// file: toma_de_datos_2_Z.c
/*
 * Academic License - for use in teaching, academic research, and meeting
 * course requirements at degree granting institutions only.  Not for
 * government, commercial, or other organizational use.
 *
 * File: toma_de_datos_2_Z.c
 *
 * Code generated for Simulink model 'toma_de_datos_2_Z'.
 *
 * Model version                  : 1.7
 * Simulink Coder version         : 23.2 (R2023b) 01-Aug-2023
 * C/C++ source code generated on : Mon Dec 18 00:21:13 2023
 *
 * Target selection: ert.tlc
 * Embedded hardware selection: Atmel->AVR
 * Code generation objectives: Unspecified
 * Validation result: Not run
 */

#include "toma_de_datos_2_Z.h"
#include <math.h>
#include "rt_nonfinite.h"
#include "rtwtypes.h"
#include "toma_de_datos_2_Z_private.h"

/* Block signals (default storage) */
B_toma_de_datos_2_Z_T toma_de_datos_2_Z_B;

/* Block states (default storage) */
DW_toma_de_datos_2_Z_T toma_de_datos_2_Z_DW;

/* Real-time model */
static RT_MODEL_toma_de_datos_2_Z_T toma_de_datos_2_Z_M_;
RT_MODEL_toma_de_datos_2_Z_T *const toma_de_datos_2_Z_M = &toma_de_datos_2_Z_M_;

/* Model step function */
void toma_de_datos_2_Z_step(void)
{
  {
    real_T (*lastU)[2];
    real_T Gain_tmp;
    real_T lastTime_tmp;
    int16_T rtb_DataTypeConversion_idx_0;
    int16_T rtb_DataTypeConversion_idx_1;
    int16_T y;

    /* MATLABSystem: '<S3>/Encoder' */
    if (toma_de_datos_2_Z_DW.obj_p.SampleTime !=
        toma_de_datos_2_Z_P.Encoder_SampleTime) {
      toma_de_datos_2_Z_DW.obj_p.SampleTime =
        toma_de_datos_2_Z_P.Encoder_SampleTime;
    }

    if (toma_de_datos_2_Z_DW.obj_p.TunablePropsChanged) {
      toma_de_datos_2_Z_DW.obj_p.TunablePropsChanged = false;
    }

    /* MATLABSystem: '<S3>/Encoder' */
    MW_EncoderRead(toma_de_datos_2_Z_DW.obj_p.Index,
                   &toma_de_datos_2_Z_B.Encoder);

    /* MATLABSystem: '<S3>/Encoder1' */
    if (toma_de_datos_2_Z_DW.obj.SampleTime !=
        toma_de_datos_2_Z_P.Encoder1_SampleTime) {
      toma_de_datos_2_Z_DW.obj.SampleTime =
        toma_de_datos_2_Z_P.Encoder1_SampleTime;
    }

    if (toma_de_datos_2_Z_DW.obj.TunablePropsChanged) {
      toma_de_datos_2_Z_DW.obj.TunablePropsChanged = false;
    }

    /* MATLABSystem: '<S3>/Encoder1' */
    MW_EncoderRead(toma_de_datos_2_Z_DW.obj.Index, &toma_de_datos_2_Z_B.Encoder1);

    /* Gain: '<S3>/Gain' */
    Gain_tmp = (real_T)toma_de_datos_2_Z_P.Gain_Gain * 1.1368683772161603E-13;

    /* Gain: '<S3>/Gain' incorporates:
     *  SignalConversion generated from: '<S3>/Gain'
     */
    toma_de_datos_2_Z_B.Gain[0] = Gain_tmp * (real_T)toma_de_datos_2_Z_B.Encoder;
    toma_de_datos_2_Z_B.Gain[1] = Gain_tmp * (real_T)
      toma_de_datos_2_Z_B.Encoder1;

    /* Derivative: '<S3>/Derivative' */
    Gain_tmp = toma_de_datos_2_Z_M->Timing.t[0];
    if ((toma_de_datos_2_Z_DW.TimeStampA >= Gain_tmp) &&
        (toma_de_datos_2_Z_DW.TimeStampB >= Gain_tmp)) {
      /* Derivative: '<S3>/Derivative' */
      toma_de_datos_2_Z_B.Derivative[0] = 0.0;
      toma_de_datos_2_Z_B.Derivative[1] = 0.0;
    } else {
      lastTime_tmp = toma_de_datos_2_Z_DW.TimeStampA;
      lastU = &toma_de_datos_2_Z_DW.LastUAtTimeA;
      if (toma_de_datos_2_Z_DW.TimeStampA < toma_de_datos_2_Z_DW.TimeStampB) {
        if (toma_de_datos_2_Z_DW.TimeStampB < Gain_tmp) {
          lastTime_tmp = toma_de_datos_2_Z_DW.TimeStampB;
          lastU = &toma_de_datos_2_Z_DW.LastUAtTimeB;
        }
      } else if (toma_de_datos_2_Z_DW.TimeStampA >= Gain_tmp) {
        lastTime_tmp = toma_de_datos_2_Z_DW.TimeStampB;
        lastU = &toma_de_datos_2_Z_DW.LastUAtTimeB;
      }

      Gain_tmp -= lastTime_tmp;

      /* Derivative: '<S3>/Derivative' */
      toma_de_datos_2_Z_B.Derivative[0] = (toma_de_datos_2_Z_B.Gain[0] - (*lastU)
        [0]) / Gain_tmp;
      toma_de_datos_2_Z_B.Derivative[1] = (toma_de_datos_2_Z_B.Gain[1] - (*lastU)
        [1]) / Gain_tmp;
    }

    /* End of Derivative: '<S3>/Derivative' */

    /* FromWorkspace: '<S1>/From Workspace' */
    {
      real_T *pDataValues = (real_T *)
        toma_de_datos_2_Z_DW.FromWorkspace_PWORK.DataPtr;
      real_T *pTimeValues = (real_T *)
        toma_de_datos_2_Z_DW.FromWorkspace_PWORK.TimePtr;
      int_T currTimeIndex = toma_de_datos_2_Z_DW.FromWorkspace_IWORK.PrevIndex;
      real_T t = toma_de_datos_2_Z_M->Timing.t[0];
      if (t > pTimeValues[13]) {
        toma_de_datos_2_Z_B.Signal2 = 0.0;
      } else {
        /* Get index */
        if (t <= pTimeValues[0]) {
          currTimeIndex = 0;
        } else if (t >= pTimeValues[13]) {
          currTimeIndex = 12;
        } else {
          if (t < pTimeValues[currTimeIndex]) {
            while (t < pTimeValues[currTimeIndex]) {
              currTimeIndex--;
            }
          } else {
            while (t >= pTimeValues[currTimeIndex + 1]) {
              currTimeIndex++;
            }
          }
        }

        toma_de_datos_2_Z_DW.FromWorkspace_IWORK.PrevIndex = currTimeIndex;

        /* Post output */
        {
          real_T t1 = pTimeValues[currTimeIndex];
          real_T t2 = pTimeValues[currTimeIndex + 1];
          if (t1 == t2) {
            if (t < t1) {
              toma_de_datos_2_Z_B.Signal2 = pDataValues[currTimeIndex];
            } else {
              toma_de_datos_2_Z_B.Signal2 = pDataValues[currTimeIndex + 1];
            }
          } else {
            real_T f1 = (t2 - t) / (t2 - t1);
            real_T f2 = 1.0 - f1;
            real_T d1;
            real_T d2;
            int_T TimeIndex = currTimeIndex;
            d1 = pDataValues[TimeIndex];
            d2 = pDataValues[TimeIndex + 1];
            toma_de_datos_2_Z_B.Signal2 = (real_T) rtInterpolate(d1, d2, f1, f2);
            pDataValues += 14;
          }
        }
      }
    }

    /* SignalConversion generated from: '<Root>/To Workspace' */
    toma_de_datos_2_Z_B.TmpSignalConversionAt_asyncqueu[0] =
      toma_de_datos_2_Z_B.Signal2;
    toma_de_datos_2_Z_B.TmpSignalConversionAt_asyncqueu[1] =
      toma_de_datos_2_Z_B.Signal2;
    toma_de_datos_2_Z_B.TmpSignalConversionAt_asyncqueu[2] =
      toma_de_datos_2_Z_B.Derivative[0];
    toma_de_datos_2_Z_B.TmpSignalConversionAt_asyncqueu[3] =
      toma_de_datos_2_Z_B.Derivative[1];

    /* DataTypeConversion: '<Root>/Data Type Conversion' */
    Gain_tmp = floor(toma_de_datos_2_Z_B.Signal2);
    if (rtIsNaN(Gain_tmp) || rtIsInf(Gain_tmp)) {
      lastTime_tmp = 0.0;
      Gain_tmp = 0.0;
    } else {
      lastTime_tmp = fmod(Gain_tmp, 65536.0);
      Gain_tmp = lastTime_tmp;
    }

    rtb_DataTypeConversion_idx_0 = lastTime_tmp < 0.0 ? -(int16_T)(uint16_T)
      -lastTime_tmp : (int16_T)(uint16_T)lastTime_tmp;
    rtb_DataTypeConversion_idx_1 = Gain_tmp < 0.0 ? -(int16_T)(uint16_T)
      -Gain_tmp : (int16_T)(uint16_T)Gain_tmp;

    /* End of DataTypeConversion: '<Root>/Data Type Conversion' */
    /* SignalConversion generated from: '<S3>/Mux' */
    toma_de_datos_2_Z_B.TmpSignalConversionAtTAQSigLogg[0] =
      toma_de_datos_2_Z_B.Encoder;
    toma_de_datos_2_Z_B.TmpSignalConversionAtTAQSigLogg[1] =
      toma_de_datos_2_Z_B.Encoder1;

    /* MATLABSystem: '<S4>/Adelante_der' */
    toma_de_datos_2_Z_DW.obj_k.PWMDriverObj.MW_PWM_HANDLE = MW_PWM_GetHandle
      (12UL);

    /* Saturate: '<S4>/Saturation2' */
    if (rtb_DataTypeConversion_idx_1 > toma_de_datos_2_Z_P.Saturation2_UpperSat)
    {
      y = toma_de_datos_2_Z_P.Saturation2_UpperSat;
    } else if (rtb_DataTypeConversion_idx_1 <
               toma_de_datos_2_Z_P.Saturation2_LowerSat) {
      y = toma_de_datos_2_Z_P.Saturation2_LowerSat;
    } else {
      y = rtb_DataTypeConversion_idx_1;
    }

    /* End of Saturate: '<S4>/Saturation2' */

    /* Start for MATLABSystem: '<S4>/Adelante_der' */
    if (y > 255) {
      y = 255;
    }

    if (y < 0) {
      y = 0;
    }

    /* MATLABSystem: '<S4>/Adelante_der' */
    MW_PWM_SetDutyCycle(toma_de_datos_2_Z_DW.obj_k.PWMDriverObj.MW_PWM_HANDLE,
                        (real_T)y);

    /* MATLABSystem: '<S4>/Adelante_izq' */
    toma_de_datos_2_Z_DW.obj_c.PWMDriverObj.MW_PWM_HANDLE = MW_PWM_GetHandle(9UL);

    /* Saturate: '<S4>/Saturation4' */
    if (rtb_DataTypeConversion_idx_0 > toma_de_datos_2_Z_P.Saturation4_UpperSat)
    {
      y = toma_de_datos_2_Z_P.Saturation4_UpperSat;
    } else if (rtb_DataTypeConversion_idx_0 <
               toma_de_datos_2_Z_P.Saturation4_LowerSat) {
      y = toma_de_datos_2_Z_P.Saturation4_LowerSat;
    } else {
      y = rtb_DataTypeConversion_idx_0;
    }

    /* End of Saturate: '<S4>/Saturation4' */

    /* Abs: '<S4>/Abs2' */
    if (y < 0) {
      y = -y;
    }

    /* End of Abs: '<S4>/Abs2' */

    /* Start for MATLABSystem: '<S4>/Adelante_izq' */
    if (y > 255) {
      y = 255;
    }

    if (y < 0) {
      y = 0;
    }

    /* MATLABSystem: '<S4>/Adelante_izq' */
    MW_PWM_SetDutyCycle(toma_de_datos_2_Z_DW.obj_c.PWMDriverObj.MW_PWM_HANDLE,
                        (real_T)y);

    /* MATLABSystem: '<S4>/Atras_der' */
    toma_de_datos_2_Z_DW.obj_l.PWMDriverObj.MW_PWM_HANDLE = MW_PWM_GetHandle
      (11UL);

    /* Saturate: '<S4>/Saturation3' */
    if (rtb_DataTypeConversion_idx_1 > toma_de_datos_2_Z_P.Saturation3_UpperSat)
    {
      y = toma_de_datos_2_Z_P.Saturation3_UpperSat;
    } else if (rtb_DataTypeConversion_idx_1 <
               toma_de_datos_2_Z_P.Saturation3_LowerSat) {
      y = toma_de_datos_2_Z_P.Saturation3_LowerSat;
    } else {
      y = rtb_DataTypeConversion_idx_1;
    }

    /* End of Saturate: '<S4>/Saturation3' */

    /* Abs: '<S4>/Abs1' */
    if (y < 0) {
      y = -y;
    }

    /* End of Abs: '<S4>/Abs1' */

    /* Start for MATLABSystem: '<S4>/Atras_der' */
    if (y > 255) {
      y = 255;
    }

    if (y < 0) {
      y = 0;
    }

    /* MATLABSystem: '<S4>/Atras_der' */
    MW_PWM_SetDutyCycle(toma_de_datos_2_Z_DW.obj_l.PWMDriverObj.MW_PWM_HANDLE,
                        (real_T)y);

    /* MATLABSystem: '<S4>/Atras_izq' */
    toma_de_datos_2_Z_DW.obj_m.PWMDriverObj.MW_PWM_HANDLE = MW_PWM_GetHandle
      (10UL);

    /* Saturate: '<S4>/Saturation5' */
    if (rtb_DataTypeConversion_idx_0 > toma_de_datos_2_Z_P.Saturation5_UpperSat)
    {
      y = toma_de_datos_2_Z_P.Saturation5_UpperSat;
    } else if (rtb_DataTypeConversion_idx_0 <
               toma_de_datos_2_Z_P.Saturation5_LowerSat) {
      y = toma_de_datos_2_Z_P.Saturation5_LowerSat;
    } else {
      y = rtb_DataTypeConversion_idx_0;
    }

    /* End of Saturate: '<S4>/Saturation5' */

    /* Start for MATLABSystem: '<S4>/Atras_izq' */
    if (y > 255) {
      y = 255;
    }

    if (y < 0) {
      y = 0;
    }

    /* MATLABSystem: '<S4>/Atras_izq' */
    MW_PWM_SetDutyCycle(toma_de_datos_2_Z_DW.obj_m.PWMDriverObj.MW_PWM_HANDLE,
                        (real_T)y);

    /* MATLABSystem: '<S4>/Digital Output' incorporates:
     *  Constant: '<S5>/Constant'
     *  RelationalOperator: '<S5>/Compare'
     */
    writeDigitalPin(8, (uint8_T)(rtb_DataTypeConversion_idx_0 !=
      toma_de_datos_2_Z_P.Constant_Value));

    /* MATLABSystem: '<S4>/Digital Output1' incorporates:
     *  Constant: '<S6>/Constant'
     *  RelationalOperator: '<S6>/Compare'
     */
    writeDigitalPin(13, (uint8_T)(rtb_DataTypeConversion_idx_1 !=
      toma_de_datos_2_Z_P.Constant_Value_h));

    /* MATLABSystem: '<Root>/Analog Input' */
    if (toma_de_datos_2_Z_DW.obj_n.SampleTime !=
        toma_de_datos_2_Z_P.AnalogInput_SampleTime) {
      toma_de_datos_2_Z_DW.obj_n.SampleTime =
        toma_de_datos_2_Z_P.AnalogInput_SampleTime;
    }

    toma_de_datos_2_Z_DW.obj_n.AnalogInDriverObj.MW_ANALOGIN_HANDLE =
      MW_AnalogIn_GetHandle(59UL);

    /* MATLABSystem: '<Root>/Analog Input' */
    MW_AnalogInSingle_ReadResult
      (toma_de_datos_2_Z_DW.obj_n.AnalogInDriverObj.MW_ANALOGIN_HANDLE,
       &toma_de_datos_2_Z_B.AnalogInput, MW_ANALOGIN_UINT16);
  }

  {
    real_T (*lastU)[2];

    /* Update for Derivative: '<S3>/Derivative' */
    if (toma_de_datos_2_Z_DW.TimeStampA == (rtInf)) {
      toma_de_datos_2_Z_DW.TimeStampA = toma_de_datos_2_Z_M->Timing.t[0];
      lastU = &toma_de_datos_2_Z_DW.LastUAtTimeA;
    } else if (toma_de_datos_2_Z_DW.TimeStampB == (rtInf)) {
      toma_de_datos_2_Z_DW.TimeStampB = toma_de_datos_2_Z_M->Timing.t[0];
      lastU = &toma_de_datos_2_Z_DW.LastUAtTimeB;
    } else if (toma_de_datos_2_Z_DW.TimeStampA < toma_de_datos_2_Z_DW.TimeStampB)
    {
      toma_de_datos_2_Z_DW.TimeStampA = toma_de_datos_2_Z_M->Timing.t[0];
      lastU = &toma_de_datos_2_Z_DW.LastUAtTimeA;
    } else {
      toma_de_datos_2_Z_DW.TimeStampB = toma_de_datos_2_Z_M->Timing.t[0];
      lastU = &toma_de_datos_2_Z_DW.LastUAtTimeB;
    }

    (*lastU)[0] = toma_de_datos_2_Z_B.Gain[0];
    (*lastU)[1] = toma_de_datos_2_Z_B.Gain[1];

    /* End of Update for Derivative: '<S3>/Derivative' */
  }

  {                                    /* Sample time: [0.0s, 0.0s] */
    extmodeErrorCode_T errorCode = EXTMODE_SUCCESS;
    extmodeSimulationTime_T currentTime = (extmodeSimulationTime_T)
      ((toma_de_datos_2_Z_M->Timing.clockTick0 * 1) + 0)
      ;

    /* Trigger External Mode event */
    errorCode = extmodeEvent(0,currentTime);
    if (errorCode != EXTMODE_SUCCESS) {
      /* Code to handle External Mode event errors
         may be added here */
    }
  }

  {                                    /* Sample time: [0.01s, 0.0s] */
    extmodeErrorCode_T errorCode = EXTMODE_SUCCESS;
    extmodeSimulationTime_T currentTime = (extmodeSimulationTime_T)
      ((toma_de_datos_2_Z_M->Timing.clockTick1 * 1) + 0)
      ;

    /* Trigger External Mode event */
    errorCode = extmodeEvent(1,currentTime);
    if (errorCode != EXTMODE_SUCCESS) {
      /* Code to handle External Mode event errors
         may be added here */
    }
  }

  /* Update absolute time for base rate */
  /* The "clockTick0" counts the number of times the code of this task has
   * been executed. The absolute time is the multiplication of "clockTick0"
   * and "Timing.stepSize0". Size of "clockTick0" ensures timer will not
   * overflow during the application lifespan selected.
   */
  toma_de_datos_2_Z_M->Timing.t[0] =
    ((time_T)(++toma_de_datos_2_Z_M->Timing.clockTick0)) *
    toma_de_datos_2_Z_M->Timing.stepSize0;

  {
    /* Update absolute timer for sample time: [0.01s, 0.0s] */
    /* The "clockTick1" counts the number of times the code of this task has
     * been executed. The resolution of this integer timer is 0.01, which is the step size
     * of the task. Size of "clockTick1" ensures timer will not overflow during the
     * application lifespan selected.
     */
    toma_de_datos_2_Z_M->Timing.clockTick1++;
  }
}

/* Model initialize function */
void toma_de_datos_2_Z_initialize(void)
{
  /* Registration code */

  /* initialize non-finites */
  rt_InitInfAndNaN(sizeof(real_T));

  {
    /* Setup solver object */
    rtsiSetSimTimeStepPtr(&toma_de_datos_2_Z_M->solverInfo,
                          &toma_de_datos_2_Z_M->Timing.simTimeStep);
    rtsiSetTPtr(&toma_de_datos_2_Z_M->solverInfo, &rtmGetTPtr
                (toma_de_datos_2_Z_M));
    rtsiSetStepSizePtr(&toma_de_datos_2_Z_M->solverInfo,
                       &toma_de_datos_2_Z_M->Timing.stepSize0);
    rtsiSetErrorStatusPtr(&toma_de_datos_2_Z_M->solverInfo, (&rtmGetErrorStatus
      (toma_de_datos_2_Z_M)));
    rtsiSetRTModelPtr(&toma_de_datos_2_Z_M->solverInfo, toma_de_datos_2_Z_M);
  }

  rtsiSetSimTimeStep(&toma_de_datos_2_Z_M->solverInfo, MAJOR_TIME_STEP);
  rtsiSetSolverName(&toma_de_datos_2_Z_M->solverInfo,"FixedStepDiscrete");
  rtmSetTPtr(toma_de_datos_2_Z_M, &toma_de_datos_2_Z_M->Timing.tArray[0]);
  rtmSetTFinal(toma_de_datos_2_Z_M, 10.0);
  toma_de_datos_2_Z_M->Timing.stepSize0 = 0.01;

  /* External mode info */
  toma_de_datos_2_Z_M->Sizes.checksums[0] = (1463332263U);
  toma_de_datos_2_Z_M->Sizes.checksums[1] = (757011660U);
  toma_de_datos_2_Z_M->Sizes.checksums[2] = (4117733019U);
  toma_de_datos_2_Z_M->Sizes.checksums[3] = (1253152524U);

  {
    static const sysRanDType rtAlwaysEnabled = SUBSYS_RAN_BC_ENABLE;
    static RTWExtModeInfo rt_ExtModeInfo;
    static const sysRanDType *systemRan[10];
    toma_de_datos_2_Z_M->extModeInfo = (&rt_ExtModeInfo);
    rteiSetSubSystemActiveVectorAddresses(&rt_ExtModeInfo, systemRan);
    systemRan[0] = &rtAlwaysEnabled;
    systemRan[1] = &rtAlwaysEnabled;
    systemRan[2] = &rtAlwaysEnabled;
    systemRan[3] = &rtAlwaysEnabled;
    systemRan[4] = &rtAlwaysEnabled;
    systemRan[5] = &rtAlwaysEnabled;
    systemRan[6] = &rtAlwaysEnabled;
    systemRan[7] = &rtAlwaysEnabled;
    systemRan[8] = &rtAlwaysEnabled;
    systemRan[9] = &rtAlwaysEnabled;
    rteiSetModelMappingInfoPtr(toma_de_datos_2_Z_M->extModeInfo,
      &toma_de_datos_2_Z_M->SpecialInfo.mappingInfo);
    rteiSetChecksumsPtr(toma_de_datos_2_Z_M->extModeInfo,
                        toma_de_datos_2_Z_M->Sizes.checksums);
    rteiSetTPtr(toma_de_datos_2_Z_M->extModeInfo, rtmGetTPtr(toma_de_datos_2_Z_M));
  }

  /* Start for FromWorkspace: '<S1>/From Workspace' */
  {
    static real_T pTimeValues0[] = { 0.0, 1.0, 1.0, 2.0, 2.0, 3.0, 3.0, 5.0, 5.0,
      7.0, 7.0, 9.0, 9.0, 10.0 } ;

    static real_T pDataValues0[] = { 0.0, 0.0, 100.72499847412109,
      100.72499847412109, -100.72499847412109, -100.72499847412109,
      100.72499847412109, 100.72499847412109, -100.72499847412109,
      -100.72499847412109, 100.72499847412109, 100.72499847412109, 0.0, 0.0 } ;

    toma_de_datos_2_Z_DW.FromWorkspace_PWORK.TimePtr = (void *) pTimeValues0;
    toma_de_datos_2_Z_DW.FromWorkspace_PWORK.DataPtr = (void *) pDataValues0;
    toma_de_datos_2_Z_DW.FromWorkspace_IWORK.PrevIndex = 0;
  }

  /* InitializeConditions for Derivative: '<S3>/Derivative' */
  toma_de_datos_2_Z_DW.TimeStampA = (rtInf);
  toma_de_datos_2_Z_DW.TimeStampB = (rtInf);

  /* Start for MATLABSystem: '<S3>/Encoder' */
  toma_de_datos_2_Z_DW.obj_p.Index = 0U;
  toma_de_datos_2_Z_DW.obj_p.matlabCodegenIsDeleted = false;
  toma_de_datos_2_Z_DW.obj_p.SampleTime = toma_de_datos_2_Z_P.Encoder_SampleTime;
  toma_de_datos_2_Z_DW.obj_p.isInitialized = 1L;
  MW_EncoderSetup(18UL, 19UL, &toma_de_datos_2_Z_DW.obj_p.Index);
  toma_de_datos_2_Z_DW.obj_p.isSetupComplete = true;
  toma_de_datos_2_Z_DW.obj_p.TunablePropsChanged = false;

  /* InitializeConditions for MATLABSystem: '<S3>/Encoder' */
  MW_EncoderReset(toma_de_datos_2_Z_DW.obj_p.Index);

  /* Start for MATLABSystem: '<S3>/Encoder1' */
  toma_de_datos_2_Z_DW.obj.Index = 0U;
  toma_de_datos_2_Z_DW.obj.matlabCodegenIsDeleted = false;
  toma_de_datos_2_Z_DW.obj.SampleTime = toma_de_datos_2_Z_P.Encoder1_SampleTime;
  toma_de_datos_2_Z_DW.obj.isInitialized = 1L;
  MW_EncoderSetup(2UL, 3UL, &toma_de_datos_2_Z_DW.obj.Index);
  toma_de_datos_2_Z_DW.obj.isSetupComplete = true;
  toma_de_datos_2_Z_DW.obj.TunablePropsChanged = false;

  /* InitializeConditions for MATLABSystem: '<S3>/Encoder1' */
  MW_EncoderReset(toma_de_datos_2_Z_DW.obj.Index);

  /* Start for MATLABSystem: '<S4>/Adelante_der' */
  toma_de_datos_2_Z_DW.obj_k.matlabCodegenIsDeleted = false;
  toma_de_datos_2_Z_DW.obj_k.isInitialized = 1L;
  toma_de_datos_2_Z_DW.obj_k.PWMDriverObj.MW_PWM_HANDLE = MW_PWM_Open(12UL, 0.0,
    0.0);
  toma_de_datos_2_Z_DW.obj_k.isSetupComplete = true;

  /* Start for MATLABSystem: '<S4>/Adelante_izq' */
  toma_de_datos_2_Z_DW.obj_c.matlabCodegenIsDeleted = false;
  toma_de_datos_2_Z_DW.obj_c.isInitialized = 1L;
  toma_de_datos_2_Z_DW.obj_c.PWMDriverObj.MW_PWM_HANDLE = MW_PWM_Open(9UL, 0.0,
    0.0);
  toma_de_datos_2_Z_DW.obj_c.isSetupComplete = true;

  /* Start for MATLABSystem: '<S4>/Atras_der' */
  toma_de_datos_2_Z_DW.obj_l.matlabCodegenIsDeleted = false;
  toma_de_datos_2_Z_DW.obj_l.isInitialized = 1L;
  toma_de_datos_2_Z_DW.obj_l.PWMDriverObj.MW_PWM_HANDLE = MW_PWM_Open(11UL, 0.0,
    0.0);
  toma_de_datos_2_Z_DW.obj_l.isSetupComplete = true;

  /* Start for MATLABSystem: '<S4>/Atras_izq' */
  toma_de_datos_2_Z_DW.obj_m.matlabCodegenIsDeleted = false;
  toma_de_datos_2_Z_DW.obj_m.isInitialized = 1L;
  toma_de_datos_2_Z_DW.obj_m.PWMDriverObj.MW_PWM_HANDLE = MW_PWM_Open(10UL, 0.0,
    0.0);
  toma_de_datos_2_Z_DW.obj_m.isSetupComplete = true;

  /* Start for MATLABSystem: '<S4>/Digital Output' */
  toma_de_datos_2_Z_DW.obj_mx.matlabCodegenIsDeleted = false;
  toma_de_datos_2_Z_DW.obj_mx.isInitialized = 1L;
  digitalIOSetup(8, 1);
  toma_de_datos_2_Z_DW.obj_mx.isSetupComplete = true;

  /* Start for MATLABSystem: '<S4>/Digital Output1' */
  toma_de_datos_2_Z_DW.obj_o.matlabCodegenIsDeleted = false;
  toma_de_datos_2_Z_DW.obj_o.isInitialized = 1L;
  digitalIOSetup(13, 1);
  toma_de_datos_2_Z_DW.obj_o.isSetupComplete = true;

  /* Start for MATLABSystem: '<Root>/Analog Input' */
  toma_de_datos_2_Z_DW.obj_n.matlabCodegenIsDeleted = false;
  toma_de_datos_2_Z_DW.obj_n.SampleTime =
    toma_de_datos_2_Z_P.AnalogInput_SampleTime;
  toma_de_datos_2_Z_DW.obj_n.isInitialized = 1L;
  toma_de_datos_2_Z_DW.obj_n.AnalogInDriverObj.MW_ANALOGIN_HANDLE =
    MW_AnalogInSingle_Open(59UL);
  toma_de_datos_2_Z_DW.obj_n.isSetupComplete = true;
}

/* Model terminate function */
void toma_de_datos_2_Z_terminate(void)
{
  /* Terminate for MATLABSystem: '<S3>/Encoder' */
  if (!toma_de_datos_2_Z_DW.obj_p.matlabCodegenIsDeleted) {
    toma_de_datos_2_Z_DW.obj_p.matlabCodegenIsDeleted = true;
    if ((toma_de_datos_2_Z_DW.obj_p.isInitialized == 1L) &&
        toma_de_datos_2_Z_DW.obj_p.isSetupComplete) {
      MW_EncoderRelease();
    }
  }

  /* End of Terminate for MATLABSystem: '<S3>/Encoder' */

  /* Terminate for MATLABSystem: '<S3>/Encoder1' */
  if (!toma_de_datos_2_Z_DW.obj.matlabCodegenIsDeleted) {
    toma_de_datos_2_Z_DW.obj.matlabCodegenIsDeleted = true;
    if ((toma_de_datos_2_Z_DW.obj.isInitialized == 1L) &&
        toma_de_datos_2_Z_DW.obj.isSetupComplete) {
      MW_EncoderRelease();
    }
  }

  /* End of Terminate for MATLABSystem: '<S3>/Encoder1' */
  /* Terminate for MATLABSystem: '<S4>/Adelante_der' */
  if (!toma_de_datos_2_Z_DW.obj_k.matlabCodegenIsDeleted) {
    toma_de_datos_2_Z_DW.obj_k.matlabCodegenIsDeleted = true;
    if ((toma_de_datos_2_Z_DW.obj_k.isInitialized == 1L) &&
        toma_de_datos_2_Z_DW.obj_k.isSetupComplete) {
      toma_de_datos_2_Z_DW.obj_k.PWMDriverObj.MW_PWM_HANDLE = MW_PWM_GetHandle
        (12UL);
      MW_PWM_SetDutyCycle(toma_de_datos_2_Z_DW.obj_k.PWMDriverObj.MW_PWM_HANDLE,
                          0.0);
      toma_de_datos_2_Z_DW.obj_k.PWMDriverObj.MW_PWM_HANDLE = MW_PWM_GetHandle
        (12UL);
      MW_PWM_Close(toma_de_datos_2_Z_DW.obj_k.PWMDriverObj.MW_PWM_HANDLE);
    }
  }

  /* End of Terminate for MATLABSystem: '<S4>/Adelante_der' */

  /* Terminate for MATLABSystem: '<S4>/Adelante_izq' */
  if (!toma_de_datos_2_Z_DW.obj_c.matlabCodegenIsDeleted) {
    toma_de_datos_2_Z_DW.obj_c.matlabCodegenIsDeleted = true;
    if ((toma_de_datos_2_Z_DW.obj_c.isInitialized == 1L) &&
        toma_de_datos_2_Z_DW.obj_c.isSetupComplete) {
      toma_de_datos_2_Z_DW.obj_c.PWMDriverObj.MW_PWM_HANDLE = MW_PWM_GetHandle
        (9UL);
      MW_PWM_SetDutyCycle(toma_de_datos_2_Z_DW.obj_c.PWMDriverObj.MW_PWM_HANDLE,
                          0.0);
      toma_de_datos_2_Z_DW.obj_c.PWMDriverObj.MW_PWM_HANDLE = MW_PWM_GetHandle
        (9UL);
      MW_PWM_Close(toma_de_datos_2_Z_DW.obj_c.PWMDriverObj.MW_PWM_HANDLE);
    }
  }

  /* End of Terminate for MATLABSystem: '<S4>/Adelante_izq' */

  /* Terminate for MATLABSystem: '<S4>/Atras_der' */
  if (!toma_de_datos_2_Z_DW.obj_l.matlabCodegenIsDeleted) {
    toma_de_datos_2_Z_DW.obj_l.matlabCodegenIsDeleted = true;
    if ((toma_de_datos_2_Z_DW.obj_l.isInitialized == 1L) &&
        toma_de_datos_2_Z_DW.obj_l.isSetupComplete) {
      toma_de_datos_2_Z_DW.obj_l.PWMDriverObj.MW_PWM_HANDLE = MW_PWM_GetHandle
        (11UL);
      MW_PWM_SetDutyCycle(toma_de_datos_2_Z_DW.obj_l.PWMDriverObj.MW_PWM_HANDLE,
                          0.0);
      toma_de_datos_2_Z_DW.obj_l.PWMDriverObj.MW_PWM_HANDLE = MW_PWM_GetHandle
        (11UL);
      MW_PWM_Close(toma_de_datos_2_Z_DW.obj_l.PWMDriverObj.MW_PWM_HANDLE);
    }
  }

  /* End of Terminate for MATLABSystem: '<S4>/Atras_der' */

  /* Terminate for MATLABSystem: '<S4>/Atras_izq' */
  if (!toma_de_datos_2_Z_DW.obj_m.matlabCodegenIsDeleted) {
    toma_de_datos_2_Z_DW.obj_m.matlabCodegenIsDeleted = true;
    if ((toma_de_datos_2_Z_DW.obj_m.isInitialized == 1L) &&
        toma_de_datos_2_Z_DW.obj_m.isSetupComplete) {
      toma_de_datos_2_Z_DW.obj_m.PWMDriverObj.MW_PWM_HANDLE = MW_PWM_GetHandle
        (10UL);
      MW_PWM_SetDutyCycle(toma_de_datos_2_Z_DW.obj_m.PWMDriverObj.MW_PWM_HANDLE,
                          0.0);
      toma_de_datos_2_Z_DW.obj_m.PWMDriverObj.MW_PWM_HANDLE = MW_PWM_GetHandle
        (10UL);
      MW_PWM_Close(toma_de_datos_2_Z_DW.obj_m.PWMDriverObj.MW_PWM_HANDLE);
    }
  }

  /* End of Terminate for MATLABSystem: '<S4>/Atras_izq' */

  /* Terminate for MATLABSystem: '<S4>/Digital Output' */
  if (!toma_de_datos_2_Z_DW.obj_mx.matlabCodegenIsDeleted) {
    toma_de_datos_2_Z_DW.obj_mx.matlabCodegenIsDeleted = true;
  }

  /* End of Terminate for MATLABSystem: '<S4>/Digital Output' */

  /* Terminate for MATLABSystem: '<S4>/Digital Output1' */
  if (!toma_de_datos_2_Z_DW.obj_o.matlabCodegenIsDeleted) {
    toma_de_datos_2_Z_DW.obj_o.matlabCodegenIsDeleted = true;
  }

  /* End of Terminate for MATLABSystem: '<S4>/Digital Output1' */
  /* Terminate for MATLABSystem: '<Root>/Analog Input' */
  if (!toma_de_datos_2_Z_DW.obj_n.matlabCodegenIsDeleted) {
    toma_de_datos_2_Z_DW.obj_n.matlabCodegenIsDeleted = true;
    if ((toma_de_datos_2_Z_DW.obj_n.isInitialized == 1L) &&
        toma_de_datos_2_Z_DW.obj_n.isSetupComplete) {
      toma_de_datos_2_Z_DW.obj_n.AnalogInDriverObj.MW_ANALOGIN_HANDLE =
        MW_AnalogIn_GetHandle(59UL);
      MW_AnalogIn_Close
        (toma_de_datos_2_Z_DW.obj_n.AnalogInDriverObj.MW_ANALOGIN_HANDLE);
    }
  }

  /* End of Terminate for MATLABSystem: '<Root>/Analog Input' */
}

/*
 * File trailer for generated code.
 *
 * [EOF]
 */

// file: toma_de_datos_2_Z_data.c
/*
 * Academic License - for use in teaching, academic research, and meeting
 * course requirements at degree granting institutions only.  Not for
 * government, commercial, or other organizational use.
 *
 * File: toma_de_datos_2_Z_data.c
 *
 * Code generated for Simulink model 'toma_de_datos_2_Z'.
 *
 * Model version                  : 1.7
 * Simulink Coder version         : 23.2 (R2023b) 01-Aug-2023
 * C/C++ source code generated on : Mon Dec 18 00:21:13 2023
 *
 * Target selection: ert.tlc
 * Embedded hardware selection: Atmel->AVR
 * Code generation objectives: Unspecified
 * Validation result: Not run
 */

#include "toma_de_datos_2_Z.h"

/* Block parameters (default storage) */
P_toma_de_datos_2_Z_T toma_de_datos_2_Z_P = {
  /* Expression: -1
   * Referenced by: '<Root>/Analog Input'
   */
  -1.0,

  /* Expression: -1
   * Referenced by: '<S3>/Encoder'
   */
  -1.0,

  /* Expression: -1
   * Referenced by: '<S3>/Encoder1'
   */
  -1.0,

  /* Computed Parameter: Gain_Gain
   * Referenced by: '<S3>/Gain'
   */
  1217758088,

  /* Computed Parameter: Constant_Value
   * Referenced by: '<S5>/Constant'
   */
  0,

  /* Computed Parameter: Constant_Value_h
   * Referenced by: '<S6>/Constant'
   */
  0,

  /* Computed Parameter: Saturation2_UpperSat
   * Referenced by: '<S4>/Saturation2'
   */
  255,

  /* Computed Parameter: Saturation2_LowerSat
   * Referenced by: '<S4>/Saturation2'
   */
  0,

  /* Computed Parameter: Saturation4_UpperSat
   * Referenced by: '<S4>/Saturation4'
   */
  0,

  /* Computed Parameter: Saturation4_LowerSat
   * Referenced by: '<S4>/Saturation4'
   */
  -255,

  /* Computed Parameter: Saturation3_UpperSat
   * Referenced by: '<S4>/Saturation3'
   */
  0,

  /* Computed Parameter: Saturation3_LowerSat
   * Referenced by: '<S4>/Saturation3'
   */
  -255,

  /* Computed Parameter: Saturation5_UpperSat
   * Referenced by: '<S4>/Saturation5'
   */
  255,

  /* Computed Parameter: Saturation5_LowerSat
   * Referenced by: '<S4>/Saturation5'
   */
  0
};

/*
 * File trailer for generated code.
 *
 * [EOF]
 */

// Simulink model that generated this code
simulink model "toma_de_datos_2_Z"  (R2023b)
settings: Solver=FixedStepAuto  StartTime=0.0  StopTime=10  FixedStep=0.01  RelTol=1e-3  EnableMultiTasking=on
libraries: arduinolib x1, SignalEditorBlockLib x1

== system toma_de_datos_2_Z ==
  Analog Input : arduinolib/Analog Input  pinNumber=5  ReadResultsOnly=off  ConversionTriggerSource=Software  ExternalTriggerType=uint32( 0 )  OutputDataType=uint16  EnableConversionCompleteNotify=off  EnableOuputStatus=off  SampleTime=-1  blockPlatform=arduino
  Data Type Conversion : DataTypeConversion  OutDataTypeStr=int16  SaturateOnIntegerOverflow=off  RndMeth=Floor
  Display : Display
  Mux : Mux  Inputs=2
  Mux1 : Mux  Inputs=2
  Scope : Scope  NumInputPorts=2
  Signal Editor : SignalEditorBlockLib/Signal Editor  FileName=Siganl_PWM_H2.mat  ActiveScenario=Scenario  ActiveSignal=Signal 2  IsBus=off  OutputBusObjectStr=Bus: BusObject  SampleTime=0  OutputAfterFinalValue=Setting to zero  Unit=inherit  PreserveSignalName=on  ApplySigPropsToAllScenarios=on  ApplySigPropsToAllSignals=off
  Subsystem Reference : Subsystem  ReferencedSubsystem=Piero_Hardware
  To Workspace : ToWorkspace  VariableName=simout  SampleTime=-1
  wires:
  Mux/1 -> Mux1/1, Data Type Conversion/1
  Data Type Conversion/1 -> Subsystem Reference/1
  Subsystem Reference/1 -> Scope/1, Mux1/2
  Mux1/1 -> To Workspace/1
  Signal Editor/2 -> Scope/2, Mux/2, Mux/1
  Analog Input/1 -> Display/1
